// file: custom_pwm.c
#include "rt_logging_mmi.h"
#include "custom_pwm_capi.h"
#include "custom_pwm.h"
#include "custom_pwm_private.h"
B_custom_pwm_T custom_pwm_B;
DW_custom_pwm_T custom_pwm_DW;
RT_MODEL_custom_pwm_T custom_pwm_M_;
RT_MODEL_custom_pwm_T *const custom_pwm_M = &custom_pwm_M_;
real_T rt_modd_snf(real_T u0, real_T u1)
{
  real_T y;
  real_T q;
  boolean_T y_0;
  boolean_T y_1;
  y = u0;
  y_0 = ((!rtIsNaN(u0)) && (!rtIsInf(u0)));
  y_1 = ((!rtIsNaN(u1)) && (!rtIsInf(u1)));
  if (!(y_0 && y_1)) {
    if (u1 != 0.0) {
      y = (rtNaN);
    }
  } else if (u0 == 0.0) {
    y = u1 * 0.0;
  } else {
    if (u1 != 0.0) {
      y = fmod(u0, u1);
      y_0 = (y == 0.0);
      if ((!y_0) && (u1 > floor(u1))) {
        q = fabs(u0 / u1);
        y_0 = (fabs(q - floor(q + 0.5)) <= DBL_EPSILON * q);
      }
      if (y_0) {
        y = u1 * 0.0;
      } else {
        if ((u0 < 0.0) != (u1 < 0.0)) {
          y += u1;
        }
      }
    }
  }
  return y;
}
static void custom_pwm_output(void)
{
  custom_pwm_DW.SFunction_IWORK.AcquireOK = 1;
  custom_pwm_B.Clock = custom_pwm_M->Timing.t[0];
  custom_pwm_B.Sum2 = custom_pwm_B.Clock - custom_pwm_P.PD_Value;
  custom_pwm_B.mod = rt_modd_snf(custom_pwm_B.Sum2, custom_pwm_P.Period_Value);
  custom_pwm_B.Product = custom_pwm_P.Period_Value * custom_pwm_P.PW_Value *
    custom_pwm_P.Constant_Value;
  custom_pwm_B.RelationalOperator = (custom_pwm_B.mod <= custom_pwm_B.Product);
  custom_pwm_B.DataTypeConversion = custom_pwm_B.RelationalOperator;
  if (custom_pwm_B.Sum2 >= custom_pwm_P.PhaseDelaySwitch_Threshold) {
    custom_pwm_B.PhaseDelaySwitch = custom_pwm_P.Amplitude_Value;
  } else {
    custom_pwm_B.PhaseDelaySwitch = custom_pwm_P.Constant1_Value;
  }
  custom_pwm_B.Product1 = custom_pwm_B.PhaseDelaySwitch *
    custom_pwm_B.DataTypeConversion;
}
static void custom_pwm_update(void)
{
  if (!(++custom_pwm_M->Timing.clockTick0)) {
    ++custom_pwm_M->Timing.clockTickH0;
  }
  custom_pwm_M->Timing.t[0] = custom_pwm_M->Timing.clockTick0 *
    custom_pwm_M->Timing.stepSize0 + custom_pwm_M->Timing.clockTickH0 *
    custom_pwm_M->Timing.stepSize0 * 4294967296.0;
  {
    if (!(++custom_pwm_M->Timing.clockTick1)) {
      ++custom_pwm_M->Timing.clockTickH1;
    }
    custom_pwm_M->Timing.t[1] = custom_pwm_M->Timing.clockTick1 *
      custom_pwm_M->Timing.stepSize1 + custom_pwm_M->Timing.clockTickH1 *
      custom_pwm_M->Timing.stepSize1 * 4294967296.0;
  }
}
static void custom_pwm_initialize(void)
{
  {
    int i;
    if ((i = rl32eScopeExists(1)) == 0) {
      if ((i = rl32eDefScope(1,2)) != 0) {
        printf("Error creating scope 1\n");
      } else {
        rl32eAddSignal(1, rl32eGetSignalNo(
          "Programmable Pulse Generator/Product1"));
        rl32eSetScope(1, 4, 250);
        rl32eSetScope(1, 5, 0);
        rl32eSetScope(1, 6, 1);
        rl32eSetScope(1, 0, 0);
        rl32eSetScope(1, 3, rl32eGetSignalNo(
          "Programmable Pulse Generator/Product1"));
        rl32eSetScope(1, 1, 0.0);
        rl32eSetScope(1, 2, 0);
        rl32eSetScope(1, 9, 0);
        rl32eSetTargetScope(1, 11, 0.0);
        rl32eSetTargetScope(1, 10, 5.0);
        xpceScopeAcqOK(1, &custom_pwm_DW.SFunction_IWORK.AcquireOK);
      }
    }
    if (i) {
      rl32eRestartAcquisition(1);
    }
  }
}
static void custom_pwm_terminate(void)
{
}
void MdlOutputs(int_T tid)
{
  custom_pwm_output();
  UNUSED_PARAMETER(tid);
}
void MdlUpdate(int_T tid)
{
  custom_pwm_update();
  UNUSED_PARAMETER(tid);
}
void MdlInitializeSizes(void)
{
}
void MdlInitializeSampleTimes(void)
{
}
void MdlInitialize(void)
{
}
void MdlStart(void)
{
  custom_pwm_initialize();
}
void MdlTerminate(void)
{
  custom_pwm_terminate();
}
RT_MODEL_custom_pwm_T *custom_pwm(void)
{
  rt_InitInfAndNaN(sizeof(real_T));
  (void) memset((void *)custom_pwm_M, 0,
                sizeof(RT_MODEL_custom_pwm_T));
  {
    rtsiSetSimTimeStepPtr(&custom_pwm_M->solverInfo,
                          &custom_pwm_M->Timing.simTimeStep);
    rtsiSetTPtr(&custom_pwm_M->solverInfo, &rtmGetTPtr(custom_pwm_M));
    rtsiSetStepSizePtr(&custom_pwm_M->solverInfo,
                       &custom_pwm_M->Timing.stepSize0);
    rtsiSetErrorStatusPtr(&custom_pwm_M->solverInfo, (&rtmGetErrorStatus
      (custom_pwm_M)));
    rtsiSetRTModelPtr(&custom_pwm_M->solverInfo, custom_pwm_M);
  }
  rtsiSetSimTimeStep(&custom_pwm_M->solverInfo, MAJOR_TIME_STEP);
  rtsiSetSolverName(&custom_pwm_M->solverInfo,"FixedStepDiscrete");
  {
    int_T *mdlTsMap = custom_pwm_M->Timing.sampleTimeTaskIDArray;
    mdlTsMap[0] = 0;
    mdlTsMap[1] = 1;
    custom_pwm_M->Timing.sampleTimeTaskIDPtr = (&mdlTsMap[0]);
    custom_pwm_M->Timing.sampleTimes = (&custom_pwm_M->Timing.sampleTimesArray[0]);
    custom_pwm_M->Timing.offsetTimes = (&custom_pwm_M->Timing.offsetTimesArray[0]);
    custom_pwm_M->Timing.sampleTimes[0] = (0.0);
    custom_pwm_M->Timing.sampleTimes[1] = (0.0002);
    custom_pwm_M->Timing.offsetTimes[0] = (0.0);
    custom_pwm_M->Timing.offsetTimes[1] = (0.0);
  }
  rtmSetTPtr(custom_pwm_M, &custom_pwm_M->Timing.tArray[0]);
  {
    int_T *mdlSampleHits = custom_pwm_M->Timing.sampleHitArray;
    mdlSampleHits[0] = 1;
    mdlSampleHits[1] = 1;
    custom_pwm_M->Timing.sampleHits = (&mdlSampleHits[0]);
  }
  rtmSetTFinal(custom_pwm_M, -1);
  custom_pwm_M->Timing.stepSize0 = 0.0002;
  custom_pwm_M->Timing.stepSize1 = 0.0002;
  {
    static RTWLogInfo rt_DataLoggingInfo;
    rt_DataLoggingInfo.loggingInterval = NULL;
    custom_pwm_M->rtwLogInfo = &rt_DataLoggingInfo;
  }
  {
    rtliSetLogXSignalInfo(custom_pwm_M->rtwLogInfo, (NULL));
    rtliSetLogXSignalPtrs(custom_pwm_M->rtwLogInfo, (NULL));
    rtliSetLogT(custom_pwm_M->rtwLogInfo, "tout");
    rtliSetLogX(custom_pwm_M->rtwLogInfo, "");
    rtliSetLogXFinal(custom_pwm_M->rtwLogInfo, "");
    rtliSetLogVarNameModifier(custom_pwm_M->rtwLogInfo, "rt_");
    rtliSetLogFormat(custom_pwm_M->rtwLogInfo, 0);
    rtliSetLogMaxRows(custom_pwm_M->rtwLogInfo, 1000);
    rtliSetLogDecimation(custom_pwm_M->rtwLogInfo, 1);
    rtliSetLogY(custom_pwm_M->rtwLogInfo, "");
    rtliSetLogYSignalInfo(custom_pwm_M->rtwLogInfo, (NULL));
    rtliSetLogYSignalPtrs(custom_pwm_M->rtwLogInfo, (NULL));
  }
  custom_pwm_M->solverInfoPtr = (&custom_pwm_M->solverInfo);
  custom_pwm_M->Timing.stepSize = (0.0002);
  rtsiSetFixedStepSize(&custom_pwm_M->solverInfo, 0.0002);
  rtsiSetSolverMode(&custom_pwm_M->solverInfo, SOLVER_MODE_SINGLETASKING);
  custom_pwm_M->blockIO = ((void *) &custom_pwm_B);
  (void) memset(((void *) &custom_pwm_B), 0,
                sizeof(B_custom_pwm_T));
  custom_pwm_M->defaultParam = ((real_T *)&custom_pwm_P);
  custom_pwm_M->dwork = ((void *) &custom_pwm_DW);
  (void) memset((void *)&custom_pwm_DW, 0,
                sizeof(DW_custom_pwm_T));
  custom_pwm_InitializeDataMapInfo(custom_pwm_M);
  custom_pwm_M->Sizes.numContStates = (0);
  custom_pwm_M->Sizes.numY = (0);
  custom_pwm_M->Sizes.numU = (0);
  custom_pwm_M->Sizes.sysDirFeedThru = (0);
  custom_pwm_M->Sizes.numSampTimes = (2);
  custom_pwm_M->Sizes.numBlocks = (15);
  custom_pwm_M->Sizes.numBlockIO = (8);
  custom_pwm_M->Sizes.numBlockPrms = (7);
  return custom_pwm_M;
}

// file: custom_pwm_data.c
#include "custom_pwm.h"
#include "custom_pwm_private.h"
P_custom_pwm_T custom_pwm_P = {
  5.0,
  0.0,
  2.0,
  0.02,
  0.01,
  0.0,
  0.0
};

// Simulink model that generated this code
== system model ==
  Product1 : Product  <- 1: PhaseDelaySwitch, 2: DataTypeConversion
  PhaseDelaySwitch : Switch  <- 1: Amplitude, 2: Sum2, 3: Constant1
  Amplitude : Constant  Value=5
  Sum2 : Sum  Inputs=+-  <- 1: Clock, 2: PD
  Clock : Clock
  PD : Constant  Value=0
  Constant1 : Constant  Value=0
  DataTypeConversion : DataTypeConversion  <- 1: RelationalOperator
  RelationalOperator : RelationalOperator  Operator=<=  <- 1: mod, 2: Product
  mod : Math  Operator=mod  <- 1: Sum2, 2: Period
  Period : Constant  Value=0.02
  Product : Product  Inputs=3  <- 1: Period, 2: PW, 3: Constant
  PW : Constant  Value=2
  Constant : Constant  Value=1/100
